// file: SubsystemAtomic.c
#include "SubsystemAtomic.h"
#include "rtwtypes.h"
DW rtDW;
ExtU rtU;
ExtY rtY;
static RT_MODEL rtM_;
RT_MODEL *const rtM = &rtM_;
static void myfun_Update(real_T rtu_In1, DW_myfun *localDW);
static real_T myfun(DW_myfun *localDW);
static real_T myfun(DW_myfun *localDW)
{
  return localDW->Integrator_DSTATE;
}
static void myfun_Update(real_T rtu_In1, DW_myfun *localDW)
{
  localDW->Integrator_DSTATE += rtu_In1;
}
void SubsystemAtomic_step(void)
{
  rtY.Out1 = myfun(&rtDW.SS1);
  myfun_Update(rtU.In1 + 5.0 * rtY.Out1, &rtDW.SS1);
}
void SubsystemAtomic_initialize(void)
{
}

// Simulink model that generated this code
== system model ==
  In1 : Inport
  Out1 : Outport  <- 1: SS1
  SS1 : Subsystem  <- 1: Sum#1
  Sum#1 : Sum  Inputs=++  <- 1: In1, 2: Gain#1
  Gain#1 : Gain  Gain=5  <- 1: SS1
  BuildERT#1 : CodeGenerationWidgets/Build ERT
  BuildGRT#1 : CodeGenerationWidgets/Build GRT
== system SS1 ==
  Inport#1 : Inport
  Outport#1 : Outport  <- 1: Integrator
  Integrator : DiscreteIntegrator  <- 1: Inport#1
